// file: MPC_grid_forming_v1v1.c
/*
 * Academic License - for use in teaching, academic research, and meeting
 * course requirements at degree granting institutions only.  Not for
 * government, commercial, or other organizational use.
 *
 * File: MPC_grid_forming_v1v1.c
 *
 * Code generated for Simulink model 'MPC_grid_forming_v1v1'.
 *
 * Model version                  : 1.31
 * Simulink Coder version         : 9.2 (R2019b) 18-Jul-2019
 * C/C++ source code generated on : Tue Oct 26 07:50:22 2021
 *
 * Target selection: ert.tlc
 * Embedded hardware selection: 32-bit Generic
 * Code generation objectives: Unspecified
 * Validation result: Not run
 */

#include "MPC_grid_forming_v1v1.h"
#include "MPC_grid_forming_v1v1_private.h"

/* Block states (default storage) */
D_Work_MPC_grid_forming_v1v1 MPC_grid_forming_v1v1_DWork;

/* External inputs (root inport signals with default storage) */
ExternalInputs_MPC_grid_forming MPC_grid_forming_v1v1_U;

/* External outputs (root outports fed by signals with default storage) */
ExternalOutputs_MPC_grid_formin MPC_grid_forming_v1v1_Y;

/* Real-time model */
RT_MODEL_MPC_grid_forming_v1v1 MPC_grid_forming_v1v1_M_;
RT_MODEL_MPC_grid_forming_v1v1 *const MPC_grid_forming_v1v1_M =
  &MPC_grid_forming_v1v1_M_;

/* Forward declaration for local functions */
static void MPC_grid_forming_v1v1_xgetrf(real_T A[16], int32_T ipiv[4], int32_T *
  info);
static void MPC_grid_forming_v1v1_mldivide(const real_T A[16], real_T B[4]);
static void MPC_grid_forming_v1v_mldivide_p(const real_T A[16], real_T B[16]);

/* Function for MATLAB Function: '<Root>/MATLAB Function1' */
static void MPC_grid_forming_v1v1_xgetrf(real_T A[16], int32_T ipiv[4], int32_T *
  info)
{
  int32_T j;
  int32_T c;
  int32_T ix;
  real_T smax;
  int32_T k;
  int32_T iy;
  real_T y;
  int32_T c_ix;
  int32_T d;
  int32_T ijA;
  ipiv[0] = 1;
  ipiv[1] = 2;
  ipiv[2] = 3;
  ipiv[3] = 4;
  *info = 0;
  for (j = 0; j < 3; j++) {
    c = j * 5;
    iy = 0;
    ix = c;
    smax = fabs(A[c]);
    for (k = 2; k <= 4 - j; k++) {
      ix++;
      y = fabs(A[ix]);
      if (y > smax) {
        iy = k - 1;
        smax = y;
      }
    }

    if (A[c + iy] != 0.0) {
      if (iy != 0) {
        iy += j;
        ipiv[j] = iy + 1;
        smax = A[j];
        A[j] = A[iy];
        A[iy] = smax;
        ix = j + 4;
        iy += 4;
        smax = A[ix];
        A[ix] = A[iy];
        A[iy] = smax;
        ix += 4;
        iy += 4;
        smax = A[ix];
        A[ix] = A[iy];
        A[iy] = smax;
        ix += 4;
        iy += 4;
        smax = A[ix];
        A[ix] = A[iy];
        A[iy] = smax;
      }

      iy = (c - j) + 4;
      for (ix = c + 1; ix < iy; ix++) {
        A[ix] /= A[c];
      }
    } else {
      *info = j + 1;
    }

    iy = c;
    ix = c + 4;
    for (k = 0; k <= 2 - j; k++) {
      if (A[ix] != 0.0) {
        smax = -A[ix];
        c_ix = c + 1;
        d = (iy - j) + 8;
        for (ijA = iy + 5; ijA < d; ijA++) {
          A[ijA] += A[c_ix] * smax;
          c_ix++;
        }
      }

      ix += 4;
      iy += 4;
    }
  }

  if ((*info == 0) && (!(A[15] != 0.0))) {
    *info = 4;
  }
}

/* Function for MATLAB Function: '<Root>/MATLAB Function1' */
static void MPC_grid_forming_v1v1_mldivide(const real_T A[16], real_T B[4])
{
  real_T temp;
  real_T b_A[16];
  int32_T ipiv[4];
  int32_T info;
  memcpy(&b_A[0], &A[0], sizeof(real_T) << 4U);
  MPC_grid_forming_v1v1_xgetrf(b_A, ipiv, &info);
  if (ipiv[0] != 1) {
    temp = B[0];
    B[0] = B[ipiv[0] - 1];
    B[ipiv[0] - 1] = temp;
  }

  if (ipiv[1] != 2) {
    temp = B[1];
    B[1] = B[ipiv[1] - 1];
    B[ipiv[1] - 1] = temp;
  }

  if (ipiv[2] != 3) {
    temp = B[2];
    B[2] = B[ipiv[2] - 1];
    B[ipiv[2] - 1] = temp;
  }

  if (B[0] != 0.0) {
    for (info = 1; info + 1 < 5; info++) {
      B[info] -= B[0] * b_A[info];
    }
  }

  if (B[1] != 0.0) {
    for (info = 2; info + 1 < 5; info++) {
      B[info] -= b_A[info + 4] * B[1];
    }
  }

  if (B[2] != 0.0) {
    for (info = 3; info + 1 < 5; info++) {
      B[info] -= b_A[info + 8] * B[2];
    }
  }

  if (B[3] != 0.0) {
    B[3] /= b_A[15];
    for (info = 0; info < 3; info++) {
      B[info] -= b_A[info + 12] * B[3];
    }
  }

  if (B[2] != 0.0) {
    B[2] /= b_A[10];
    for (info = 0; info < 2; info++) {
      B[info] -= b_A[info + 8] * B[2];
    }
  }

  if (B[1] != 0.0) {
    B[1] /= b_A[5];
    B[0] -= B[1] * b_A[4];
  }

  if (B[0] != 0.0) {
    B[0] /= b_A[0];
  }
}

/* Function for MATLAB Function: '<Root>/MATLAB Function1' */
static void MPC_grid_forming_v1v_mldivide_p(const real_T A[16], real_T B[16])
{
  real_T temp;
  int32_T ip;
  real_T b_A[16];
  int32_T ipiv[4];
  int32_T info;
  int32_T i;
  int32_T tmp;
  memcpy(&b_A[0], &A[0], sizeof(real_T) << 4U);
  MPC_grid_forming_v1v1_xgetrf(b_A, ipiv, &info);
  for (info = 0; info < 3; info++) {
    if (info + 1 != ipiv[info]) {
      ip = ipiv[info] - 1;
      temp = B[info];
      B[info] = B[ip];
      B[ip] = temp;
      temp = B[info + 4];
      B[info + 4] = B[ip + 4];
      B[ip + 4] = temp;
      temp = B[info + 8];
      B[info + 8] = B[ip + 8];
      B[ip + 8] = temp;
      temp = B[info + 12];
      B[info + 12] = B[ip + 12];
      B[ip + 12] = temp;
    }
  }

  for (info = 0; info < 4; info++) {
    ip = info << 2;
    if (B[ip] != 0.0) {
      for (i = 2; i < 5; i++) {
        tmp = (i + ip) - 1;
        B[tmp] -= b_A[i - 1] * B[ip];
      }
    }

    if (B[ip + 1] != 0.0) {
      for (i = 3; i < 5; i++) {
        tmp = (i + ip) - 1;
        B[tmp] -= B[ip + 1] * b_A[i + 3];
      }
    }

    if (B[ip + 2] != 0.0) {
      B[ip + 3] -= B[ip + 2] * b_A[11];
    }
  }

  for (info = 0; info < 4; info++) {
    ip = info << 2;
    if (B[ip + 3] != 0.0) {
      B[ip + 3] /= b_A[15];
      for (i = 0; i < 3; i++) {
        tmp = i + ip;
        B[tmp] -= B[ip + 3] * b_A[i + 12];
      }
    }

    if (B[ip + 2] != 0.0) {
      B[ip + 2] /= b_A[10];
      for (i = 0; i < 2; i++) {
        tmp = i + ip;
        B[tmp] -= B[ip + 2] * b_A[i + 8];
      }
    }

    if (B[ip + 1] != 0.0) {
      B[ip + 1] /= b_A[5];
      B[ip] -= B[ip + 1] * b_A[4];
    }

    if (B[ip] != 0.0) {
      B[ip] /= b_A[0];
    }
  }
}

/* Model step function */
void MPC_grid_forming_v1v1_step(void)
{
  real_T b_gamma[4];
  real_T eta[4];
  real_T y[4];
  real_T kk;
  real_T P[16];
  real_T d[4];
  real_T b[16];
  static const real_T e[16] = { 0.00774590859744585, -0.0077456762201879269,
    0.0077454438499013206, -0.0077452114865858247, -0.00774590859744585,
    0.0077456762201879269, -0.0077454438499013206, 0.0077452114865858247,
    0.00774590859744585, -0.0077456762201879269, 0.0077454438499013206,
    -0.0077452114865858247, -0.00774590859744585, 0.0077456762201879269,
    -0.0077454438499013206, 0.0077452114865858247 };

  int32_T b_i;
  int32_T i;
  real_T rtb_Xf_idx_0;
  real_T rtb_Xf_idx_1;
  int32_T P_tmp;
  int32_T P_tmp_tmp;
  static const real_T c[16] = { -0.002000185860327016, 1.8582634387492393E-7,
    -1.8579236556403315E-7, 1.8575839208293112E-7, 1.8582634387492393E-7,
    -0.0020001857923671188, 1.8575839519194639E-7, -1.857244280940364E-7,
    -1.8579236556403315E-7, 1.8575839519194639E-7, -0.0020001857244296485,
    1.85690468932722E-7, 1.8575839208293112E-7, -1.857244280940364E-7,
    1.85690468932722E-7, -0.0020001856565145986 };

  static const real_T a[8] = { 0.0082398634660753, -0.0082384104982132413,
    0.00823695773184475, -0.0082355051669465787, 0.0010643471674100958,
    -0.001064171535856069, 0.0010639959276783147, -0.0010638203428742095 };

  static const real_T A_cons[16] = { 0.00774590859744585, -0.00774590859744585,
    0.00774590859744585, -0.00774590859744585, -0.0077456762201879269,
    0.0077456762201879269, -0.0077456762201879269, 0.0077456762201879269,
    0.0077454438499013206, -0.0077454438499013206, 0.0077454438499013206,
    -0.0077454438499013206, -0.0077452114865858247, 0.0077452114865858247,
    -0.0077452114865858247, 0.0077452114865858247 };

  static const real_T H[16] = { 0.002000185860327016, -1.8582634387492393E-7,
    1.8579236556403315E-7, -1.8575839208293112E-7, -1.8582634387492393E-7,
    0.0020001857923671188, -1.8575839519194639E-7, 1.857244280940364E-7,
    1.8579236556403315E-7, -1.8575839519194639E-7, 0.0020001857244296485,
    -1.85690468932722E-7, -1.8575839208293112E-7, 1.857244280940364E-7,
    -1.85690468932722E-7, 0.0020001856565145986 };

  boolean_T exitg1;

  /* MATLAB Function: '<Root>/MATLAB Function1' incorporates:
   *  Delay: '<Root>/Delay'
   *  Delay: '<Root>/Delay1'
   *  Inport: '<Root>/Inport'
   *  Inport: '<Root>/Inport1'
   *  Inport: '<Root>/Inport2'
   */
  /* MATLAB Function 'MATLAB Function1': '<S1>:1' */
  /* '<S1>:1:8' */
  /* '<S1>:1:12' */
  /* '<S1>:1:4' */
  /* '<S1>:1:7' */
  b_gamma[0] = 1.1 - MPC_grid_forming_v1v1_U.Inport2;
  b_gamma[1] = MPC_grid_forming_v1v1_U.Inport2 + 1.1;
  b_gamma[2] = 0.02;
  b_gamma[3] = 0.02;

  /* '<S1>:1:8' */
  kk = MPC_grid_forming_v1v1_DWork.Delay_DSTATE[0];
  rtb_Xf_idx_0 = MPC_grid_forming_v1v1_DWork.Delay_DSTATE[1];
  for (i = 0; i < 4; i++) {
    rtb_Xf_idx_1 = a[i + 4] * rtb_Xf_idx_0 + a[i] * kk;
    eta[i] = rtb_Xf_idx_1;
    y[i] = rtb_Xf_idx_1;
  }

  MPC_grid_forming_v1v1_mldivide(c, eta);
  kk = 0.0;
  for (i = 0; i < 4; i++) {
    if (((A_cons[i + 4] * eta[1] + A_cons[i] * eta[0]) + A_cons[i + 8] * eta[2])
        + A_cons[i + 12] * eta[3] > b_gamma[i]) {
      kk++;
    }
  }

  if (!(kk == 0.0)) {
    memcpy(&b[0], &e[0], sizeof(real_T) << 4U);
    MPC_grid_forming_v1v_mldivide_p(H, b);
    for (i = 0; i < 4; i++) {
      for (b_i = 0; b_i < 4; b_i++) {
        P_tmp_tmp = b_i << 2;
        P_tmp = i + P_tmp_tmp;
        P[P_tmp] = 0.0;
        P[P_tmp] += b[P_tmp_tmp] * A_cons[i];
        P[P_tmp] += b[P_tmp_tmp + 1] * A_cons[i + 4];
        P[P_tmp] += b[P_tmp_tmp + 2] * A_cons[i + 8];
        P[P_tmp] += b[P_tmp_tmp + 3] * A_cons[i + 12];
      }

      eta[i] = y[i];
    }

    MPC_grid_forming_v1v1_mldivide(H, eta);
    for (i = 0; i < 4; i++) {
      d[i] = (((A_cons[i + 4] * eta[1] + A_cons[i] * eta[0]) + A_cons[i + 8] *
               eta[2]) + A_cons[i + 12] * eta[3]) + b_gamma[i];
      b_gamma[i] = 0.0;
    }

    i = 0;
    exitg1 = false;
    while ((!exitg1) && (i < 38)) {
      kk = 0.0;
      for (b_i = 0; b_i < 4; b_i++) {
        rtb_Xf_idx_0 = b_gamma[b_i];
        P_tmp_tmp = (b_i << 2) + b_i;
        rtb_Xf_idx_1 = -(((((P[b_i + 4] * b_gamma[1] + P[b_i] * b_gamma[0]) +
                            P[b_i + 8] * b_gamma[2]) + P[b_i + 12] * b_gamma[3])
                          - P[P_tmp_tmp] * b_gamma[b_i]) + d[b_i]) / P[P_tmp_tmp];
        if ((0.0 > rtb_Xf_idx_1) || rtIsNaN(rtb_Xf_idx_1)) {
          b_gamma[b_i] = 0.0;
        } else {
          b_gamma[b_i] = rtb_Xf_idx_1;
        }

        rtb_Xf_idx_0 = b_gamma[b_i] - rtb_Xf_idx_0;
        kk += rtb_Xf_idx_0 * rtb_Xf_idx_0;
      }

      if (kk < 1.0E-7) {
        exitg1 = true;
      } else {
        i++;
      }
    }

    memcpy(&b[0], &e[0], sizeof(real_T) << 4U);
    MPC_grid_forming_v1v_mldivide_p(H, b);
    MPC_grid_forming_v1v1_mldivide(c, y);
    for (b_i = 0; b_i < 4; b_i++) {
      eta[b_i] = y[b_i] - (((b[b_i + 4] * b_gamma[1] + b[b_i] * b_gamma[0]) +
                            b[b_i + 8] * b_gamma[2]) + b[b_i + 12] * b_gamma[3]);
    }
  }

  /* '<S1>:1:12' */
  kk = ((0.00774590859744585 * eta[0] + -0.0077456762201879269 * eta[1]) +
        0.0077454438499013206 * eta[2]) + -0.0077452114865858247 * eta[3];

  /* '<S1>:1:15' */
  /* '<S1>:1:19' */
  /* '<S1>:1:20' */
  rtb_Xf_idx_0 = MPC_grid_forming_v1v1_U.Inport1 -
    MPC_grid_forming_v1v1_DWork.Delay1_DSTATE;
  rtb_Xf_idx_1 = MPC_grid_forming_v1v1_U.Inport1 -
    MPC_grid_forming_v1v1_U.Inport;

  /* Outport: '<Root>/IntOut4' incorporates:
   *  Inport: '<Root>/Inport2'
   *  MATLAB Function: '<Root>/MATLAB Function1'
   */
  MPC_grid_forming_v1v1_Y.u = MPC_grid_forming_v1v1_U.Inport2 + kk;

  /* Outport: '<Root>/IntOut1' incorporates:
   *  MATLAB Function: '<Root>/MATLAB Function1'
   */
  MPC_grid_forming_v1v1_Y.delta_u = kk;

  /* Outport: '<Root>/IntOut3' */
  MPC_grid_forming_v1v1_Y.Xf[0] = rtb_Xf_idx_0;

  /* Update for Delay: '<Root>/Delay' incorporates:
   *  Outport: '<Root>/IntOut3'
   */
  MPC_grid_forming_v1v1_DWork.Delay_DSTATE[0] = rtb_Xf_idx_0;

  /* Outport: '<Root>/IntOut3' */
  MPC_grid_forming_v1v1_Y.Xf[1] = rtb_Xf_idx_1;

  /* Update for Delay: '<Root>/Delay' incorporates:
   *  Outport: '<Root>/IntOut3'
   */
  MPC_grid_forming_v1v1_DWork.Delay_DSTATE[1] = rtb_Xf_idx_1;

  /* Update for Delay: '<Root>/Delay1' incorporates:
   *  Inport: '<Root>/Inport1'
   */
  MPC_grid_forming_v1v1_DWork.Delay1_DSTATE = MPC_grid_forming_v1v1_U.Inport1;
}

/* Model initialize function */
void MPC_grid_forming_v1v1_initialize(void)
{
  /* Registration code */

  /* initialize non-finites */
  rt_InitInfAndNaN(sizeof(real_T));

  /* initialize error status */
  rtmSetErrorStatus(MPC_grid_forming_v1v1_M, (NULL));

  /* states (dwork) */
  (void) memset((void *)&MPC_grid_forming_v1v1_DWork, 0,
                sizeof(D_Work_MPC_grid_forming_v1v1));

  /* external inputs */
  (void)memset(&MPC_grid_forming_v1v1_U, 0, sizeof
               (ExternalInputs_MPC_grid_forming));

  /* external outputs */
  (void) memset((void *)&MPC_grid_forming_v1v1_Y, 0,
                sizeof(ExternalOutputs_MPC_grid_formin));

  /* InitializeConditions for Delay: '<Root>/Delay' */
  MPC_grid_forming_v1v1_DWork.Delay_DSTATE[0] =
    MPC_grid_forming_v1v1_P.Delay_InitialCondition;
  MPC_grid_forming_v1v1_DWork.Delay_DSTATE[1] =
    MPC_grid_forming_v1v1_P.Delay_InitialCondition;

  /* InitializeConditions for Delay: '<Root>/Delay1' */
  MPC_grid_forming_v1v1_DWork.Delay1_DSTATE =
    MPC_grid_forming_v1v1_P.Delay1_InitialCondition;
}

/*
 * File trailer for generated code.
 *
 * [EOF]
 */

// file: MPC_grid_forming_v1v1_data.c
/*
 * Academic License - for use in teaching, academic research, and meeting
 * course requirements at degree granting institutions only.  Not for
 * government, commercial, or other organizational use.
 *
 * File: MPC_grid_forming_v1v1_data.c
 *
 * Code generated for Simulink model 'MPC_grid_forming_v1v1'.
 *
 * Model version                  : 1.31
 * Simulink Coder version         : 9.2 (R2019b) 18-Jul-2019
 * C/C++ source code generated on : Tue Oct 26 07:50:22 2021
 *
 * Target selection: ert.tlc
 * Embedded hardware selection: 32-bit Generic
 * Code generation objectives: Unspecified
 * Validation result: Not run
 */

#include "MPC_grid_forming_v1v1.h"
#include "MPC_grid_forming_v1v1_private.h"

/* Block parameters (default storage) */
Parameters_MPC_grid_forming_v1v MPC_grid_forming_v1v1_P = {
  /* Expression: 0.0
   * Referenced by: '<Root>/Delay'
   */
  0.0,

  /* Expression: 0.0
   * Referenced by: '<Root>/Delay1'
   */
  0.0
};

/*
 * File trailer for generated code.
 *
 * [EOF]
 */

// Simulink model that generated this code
simulink model "MPC_grid_forming_v1v1"  (R2019b)
settings: Solver=ode3  StartTime=0.0  StopTime=3  FixedStep=0.000050  RelTol=1e-3  EnableMultiTasking=on

== system MPC_grid_forming_v1v1 ==
  Inport : Inport
  Inport1 : Inport  Port=2
  Inport2 : Inport  Port=3
  Delay : Delay  DelayLength=1  SampleTime=50e-6
  Delay1 : Delay  DelayLength=1  SampleTime=50e-6
  MATLAB Function1 : MATLAB Function  TreatAsAtomicUnit=on
  IntOut3 : Outport  SignalName=Xf
  IntOut4 : Outport  Port=2  SignalName=u
  IntOut1 : Outport  Port=3  SignalName=delta_u
  wires:
  Inport/1 -> MATLAB Function1/1(r)
  MATLAB Function1/1(Xf) -> Delay/1, IntOut3/1
  MATLAB Function1/3(deltau) -> IntOut1/1
  Delay1/1 -> MATLAB Function1/5(Xm_k_1)
  Delay/1 -> MATLAB Function1/3(Xf_old)
  MATLAB Function1/2(u) -> IntOut4/1
  Inport1/1 -> Delay1/1, MATLAB Function1/2(xm_old)
  Inport2/1 -> MATLAB Function1/4(u_old)

== matlab function MPC_grid_forming_v1v1/MATLAB Function1 ==
function [Xf,u,deltau] = fcn(r,xm_old,Xf_old,u_old,Xm_k_1)

in = [];
in = coder.load('Grid_forming.mat'); 
%in = coder.load('DC_volatge.mat'); 
%% there is issue there which need to be fixed %%%
gamma=[(in.u_max - u_old);(-in.u_min + u_old); in.deltau_max; -in.deltau_min];
eta=QPhild(in.Omega,in.Psi*(in.Xf+Xf_old),in.M,gamma)
%%
%eta = -(in.Omega\in.Psi)*(in.Xf+Xf_old)  %%% original %%% 

deltau=in.Lzerot*eta; %%%% input signal 

%%
u=in.up+u_old+deltau;
%%%%
y = xm_old;
xm = xm_old;
y_delta_k = y-Xm_k_1;
Xf=[y_delta_k;y-r];
